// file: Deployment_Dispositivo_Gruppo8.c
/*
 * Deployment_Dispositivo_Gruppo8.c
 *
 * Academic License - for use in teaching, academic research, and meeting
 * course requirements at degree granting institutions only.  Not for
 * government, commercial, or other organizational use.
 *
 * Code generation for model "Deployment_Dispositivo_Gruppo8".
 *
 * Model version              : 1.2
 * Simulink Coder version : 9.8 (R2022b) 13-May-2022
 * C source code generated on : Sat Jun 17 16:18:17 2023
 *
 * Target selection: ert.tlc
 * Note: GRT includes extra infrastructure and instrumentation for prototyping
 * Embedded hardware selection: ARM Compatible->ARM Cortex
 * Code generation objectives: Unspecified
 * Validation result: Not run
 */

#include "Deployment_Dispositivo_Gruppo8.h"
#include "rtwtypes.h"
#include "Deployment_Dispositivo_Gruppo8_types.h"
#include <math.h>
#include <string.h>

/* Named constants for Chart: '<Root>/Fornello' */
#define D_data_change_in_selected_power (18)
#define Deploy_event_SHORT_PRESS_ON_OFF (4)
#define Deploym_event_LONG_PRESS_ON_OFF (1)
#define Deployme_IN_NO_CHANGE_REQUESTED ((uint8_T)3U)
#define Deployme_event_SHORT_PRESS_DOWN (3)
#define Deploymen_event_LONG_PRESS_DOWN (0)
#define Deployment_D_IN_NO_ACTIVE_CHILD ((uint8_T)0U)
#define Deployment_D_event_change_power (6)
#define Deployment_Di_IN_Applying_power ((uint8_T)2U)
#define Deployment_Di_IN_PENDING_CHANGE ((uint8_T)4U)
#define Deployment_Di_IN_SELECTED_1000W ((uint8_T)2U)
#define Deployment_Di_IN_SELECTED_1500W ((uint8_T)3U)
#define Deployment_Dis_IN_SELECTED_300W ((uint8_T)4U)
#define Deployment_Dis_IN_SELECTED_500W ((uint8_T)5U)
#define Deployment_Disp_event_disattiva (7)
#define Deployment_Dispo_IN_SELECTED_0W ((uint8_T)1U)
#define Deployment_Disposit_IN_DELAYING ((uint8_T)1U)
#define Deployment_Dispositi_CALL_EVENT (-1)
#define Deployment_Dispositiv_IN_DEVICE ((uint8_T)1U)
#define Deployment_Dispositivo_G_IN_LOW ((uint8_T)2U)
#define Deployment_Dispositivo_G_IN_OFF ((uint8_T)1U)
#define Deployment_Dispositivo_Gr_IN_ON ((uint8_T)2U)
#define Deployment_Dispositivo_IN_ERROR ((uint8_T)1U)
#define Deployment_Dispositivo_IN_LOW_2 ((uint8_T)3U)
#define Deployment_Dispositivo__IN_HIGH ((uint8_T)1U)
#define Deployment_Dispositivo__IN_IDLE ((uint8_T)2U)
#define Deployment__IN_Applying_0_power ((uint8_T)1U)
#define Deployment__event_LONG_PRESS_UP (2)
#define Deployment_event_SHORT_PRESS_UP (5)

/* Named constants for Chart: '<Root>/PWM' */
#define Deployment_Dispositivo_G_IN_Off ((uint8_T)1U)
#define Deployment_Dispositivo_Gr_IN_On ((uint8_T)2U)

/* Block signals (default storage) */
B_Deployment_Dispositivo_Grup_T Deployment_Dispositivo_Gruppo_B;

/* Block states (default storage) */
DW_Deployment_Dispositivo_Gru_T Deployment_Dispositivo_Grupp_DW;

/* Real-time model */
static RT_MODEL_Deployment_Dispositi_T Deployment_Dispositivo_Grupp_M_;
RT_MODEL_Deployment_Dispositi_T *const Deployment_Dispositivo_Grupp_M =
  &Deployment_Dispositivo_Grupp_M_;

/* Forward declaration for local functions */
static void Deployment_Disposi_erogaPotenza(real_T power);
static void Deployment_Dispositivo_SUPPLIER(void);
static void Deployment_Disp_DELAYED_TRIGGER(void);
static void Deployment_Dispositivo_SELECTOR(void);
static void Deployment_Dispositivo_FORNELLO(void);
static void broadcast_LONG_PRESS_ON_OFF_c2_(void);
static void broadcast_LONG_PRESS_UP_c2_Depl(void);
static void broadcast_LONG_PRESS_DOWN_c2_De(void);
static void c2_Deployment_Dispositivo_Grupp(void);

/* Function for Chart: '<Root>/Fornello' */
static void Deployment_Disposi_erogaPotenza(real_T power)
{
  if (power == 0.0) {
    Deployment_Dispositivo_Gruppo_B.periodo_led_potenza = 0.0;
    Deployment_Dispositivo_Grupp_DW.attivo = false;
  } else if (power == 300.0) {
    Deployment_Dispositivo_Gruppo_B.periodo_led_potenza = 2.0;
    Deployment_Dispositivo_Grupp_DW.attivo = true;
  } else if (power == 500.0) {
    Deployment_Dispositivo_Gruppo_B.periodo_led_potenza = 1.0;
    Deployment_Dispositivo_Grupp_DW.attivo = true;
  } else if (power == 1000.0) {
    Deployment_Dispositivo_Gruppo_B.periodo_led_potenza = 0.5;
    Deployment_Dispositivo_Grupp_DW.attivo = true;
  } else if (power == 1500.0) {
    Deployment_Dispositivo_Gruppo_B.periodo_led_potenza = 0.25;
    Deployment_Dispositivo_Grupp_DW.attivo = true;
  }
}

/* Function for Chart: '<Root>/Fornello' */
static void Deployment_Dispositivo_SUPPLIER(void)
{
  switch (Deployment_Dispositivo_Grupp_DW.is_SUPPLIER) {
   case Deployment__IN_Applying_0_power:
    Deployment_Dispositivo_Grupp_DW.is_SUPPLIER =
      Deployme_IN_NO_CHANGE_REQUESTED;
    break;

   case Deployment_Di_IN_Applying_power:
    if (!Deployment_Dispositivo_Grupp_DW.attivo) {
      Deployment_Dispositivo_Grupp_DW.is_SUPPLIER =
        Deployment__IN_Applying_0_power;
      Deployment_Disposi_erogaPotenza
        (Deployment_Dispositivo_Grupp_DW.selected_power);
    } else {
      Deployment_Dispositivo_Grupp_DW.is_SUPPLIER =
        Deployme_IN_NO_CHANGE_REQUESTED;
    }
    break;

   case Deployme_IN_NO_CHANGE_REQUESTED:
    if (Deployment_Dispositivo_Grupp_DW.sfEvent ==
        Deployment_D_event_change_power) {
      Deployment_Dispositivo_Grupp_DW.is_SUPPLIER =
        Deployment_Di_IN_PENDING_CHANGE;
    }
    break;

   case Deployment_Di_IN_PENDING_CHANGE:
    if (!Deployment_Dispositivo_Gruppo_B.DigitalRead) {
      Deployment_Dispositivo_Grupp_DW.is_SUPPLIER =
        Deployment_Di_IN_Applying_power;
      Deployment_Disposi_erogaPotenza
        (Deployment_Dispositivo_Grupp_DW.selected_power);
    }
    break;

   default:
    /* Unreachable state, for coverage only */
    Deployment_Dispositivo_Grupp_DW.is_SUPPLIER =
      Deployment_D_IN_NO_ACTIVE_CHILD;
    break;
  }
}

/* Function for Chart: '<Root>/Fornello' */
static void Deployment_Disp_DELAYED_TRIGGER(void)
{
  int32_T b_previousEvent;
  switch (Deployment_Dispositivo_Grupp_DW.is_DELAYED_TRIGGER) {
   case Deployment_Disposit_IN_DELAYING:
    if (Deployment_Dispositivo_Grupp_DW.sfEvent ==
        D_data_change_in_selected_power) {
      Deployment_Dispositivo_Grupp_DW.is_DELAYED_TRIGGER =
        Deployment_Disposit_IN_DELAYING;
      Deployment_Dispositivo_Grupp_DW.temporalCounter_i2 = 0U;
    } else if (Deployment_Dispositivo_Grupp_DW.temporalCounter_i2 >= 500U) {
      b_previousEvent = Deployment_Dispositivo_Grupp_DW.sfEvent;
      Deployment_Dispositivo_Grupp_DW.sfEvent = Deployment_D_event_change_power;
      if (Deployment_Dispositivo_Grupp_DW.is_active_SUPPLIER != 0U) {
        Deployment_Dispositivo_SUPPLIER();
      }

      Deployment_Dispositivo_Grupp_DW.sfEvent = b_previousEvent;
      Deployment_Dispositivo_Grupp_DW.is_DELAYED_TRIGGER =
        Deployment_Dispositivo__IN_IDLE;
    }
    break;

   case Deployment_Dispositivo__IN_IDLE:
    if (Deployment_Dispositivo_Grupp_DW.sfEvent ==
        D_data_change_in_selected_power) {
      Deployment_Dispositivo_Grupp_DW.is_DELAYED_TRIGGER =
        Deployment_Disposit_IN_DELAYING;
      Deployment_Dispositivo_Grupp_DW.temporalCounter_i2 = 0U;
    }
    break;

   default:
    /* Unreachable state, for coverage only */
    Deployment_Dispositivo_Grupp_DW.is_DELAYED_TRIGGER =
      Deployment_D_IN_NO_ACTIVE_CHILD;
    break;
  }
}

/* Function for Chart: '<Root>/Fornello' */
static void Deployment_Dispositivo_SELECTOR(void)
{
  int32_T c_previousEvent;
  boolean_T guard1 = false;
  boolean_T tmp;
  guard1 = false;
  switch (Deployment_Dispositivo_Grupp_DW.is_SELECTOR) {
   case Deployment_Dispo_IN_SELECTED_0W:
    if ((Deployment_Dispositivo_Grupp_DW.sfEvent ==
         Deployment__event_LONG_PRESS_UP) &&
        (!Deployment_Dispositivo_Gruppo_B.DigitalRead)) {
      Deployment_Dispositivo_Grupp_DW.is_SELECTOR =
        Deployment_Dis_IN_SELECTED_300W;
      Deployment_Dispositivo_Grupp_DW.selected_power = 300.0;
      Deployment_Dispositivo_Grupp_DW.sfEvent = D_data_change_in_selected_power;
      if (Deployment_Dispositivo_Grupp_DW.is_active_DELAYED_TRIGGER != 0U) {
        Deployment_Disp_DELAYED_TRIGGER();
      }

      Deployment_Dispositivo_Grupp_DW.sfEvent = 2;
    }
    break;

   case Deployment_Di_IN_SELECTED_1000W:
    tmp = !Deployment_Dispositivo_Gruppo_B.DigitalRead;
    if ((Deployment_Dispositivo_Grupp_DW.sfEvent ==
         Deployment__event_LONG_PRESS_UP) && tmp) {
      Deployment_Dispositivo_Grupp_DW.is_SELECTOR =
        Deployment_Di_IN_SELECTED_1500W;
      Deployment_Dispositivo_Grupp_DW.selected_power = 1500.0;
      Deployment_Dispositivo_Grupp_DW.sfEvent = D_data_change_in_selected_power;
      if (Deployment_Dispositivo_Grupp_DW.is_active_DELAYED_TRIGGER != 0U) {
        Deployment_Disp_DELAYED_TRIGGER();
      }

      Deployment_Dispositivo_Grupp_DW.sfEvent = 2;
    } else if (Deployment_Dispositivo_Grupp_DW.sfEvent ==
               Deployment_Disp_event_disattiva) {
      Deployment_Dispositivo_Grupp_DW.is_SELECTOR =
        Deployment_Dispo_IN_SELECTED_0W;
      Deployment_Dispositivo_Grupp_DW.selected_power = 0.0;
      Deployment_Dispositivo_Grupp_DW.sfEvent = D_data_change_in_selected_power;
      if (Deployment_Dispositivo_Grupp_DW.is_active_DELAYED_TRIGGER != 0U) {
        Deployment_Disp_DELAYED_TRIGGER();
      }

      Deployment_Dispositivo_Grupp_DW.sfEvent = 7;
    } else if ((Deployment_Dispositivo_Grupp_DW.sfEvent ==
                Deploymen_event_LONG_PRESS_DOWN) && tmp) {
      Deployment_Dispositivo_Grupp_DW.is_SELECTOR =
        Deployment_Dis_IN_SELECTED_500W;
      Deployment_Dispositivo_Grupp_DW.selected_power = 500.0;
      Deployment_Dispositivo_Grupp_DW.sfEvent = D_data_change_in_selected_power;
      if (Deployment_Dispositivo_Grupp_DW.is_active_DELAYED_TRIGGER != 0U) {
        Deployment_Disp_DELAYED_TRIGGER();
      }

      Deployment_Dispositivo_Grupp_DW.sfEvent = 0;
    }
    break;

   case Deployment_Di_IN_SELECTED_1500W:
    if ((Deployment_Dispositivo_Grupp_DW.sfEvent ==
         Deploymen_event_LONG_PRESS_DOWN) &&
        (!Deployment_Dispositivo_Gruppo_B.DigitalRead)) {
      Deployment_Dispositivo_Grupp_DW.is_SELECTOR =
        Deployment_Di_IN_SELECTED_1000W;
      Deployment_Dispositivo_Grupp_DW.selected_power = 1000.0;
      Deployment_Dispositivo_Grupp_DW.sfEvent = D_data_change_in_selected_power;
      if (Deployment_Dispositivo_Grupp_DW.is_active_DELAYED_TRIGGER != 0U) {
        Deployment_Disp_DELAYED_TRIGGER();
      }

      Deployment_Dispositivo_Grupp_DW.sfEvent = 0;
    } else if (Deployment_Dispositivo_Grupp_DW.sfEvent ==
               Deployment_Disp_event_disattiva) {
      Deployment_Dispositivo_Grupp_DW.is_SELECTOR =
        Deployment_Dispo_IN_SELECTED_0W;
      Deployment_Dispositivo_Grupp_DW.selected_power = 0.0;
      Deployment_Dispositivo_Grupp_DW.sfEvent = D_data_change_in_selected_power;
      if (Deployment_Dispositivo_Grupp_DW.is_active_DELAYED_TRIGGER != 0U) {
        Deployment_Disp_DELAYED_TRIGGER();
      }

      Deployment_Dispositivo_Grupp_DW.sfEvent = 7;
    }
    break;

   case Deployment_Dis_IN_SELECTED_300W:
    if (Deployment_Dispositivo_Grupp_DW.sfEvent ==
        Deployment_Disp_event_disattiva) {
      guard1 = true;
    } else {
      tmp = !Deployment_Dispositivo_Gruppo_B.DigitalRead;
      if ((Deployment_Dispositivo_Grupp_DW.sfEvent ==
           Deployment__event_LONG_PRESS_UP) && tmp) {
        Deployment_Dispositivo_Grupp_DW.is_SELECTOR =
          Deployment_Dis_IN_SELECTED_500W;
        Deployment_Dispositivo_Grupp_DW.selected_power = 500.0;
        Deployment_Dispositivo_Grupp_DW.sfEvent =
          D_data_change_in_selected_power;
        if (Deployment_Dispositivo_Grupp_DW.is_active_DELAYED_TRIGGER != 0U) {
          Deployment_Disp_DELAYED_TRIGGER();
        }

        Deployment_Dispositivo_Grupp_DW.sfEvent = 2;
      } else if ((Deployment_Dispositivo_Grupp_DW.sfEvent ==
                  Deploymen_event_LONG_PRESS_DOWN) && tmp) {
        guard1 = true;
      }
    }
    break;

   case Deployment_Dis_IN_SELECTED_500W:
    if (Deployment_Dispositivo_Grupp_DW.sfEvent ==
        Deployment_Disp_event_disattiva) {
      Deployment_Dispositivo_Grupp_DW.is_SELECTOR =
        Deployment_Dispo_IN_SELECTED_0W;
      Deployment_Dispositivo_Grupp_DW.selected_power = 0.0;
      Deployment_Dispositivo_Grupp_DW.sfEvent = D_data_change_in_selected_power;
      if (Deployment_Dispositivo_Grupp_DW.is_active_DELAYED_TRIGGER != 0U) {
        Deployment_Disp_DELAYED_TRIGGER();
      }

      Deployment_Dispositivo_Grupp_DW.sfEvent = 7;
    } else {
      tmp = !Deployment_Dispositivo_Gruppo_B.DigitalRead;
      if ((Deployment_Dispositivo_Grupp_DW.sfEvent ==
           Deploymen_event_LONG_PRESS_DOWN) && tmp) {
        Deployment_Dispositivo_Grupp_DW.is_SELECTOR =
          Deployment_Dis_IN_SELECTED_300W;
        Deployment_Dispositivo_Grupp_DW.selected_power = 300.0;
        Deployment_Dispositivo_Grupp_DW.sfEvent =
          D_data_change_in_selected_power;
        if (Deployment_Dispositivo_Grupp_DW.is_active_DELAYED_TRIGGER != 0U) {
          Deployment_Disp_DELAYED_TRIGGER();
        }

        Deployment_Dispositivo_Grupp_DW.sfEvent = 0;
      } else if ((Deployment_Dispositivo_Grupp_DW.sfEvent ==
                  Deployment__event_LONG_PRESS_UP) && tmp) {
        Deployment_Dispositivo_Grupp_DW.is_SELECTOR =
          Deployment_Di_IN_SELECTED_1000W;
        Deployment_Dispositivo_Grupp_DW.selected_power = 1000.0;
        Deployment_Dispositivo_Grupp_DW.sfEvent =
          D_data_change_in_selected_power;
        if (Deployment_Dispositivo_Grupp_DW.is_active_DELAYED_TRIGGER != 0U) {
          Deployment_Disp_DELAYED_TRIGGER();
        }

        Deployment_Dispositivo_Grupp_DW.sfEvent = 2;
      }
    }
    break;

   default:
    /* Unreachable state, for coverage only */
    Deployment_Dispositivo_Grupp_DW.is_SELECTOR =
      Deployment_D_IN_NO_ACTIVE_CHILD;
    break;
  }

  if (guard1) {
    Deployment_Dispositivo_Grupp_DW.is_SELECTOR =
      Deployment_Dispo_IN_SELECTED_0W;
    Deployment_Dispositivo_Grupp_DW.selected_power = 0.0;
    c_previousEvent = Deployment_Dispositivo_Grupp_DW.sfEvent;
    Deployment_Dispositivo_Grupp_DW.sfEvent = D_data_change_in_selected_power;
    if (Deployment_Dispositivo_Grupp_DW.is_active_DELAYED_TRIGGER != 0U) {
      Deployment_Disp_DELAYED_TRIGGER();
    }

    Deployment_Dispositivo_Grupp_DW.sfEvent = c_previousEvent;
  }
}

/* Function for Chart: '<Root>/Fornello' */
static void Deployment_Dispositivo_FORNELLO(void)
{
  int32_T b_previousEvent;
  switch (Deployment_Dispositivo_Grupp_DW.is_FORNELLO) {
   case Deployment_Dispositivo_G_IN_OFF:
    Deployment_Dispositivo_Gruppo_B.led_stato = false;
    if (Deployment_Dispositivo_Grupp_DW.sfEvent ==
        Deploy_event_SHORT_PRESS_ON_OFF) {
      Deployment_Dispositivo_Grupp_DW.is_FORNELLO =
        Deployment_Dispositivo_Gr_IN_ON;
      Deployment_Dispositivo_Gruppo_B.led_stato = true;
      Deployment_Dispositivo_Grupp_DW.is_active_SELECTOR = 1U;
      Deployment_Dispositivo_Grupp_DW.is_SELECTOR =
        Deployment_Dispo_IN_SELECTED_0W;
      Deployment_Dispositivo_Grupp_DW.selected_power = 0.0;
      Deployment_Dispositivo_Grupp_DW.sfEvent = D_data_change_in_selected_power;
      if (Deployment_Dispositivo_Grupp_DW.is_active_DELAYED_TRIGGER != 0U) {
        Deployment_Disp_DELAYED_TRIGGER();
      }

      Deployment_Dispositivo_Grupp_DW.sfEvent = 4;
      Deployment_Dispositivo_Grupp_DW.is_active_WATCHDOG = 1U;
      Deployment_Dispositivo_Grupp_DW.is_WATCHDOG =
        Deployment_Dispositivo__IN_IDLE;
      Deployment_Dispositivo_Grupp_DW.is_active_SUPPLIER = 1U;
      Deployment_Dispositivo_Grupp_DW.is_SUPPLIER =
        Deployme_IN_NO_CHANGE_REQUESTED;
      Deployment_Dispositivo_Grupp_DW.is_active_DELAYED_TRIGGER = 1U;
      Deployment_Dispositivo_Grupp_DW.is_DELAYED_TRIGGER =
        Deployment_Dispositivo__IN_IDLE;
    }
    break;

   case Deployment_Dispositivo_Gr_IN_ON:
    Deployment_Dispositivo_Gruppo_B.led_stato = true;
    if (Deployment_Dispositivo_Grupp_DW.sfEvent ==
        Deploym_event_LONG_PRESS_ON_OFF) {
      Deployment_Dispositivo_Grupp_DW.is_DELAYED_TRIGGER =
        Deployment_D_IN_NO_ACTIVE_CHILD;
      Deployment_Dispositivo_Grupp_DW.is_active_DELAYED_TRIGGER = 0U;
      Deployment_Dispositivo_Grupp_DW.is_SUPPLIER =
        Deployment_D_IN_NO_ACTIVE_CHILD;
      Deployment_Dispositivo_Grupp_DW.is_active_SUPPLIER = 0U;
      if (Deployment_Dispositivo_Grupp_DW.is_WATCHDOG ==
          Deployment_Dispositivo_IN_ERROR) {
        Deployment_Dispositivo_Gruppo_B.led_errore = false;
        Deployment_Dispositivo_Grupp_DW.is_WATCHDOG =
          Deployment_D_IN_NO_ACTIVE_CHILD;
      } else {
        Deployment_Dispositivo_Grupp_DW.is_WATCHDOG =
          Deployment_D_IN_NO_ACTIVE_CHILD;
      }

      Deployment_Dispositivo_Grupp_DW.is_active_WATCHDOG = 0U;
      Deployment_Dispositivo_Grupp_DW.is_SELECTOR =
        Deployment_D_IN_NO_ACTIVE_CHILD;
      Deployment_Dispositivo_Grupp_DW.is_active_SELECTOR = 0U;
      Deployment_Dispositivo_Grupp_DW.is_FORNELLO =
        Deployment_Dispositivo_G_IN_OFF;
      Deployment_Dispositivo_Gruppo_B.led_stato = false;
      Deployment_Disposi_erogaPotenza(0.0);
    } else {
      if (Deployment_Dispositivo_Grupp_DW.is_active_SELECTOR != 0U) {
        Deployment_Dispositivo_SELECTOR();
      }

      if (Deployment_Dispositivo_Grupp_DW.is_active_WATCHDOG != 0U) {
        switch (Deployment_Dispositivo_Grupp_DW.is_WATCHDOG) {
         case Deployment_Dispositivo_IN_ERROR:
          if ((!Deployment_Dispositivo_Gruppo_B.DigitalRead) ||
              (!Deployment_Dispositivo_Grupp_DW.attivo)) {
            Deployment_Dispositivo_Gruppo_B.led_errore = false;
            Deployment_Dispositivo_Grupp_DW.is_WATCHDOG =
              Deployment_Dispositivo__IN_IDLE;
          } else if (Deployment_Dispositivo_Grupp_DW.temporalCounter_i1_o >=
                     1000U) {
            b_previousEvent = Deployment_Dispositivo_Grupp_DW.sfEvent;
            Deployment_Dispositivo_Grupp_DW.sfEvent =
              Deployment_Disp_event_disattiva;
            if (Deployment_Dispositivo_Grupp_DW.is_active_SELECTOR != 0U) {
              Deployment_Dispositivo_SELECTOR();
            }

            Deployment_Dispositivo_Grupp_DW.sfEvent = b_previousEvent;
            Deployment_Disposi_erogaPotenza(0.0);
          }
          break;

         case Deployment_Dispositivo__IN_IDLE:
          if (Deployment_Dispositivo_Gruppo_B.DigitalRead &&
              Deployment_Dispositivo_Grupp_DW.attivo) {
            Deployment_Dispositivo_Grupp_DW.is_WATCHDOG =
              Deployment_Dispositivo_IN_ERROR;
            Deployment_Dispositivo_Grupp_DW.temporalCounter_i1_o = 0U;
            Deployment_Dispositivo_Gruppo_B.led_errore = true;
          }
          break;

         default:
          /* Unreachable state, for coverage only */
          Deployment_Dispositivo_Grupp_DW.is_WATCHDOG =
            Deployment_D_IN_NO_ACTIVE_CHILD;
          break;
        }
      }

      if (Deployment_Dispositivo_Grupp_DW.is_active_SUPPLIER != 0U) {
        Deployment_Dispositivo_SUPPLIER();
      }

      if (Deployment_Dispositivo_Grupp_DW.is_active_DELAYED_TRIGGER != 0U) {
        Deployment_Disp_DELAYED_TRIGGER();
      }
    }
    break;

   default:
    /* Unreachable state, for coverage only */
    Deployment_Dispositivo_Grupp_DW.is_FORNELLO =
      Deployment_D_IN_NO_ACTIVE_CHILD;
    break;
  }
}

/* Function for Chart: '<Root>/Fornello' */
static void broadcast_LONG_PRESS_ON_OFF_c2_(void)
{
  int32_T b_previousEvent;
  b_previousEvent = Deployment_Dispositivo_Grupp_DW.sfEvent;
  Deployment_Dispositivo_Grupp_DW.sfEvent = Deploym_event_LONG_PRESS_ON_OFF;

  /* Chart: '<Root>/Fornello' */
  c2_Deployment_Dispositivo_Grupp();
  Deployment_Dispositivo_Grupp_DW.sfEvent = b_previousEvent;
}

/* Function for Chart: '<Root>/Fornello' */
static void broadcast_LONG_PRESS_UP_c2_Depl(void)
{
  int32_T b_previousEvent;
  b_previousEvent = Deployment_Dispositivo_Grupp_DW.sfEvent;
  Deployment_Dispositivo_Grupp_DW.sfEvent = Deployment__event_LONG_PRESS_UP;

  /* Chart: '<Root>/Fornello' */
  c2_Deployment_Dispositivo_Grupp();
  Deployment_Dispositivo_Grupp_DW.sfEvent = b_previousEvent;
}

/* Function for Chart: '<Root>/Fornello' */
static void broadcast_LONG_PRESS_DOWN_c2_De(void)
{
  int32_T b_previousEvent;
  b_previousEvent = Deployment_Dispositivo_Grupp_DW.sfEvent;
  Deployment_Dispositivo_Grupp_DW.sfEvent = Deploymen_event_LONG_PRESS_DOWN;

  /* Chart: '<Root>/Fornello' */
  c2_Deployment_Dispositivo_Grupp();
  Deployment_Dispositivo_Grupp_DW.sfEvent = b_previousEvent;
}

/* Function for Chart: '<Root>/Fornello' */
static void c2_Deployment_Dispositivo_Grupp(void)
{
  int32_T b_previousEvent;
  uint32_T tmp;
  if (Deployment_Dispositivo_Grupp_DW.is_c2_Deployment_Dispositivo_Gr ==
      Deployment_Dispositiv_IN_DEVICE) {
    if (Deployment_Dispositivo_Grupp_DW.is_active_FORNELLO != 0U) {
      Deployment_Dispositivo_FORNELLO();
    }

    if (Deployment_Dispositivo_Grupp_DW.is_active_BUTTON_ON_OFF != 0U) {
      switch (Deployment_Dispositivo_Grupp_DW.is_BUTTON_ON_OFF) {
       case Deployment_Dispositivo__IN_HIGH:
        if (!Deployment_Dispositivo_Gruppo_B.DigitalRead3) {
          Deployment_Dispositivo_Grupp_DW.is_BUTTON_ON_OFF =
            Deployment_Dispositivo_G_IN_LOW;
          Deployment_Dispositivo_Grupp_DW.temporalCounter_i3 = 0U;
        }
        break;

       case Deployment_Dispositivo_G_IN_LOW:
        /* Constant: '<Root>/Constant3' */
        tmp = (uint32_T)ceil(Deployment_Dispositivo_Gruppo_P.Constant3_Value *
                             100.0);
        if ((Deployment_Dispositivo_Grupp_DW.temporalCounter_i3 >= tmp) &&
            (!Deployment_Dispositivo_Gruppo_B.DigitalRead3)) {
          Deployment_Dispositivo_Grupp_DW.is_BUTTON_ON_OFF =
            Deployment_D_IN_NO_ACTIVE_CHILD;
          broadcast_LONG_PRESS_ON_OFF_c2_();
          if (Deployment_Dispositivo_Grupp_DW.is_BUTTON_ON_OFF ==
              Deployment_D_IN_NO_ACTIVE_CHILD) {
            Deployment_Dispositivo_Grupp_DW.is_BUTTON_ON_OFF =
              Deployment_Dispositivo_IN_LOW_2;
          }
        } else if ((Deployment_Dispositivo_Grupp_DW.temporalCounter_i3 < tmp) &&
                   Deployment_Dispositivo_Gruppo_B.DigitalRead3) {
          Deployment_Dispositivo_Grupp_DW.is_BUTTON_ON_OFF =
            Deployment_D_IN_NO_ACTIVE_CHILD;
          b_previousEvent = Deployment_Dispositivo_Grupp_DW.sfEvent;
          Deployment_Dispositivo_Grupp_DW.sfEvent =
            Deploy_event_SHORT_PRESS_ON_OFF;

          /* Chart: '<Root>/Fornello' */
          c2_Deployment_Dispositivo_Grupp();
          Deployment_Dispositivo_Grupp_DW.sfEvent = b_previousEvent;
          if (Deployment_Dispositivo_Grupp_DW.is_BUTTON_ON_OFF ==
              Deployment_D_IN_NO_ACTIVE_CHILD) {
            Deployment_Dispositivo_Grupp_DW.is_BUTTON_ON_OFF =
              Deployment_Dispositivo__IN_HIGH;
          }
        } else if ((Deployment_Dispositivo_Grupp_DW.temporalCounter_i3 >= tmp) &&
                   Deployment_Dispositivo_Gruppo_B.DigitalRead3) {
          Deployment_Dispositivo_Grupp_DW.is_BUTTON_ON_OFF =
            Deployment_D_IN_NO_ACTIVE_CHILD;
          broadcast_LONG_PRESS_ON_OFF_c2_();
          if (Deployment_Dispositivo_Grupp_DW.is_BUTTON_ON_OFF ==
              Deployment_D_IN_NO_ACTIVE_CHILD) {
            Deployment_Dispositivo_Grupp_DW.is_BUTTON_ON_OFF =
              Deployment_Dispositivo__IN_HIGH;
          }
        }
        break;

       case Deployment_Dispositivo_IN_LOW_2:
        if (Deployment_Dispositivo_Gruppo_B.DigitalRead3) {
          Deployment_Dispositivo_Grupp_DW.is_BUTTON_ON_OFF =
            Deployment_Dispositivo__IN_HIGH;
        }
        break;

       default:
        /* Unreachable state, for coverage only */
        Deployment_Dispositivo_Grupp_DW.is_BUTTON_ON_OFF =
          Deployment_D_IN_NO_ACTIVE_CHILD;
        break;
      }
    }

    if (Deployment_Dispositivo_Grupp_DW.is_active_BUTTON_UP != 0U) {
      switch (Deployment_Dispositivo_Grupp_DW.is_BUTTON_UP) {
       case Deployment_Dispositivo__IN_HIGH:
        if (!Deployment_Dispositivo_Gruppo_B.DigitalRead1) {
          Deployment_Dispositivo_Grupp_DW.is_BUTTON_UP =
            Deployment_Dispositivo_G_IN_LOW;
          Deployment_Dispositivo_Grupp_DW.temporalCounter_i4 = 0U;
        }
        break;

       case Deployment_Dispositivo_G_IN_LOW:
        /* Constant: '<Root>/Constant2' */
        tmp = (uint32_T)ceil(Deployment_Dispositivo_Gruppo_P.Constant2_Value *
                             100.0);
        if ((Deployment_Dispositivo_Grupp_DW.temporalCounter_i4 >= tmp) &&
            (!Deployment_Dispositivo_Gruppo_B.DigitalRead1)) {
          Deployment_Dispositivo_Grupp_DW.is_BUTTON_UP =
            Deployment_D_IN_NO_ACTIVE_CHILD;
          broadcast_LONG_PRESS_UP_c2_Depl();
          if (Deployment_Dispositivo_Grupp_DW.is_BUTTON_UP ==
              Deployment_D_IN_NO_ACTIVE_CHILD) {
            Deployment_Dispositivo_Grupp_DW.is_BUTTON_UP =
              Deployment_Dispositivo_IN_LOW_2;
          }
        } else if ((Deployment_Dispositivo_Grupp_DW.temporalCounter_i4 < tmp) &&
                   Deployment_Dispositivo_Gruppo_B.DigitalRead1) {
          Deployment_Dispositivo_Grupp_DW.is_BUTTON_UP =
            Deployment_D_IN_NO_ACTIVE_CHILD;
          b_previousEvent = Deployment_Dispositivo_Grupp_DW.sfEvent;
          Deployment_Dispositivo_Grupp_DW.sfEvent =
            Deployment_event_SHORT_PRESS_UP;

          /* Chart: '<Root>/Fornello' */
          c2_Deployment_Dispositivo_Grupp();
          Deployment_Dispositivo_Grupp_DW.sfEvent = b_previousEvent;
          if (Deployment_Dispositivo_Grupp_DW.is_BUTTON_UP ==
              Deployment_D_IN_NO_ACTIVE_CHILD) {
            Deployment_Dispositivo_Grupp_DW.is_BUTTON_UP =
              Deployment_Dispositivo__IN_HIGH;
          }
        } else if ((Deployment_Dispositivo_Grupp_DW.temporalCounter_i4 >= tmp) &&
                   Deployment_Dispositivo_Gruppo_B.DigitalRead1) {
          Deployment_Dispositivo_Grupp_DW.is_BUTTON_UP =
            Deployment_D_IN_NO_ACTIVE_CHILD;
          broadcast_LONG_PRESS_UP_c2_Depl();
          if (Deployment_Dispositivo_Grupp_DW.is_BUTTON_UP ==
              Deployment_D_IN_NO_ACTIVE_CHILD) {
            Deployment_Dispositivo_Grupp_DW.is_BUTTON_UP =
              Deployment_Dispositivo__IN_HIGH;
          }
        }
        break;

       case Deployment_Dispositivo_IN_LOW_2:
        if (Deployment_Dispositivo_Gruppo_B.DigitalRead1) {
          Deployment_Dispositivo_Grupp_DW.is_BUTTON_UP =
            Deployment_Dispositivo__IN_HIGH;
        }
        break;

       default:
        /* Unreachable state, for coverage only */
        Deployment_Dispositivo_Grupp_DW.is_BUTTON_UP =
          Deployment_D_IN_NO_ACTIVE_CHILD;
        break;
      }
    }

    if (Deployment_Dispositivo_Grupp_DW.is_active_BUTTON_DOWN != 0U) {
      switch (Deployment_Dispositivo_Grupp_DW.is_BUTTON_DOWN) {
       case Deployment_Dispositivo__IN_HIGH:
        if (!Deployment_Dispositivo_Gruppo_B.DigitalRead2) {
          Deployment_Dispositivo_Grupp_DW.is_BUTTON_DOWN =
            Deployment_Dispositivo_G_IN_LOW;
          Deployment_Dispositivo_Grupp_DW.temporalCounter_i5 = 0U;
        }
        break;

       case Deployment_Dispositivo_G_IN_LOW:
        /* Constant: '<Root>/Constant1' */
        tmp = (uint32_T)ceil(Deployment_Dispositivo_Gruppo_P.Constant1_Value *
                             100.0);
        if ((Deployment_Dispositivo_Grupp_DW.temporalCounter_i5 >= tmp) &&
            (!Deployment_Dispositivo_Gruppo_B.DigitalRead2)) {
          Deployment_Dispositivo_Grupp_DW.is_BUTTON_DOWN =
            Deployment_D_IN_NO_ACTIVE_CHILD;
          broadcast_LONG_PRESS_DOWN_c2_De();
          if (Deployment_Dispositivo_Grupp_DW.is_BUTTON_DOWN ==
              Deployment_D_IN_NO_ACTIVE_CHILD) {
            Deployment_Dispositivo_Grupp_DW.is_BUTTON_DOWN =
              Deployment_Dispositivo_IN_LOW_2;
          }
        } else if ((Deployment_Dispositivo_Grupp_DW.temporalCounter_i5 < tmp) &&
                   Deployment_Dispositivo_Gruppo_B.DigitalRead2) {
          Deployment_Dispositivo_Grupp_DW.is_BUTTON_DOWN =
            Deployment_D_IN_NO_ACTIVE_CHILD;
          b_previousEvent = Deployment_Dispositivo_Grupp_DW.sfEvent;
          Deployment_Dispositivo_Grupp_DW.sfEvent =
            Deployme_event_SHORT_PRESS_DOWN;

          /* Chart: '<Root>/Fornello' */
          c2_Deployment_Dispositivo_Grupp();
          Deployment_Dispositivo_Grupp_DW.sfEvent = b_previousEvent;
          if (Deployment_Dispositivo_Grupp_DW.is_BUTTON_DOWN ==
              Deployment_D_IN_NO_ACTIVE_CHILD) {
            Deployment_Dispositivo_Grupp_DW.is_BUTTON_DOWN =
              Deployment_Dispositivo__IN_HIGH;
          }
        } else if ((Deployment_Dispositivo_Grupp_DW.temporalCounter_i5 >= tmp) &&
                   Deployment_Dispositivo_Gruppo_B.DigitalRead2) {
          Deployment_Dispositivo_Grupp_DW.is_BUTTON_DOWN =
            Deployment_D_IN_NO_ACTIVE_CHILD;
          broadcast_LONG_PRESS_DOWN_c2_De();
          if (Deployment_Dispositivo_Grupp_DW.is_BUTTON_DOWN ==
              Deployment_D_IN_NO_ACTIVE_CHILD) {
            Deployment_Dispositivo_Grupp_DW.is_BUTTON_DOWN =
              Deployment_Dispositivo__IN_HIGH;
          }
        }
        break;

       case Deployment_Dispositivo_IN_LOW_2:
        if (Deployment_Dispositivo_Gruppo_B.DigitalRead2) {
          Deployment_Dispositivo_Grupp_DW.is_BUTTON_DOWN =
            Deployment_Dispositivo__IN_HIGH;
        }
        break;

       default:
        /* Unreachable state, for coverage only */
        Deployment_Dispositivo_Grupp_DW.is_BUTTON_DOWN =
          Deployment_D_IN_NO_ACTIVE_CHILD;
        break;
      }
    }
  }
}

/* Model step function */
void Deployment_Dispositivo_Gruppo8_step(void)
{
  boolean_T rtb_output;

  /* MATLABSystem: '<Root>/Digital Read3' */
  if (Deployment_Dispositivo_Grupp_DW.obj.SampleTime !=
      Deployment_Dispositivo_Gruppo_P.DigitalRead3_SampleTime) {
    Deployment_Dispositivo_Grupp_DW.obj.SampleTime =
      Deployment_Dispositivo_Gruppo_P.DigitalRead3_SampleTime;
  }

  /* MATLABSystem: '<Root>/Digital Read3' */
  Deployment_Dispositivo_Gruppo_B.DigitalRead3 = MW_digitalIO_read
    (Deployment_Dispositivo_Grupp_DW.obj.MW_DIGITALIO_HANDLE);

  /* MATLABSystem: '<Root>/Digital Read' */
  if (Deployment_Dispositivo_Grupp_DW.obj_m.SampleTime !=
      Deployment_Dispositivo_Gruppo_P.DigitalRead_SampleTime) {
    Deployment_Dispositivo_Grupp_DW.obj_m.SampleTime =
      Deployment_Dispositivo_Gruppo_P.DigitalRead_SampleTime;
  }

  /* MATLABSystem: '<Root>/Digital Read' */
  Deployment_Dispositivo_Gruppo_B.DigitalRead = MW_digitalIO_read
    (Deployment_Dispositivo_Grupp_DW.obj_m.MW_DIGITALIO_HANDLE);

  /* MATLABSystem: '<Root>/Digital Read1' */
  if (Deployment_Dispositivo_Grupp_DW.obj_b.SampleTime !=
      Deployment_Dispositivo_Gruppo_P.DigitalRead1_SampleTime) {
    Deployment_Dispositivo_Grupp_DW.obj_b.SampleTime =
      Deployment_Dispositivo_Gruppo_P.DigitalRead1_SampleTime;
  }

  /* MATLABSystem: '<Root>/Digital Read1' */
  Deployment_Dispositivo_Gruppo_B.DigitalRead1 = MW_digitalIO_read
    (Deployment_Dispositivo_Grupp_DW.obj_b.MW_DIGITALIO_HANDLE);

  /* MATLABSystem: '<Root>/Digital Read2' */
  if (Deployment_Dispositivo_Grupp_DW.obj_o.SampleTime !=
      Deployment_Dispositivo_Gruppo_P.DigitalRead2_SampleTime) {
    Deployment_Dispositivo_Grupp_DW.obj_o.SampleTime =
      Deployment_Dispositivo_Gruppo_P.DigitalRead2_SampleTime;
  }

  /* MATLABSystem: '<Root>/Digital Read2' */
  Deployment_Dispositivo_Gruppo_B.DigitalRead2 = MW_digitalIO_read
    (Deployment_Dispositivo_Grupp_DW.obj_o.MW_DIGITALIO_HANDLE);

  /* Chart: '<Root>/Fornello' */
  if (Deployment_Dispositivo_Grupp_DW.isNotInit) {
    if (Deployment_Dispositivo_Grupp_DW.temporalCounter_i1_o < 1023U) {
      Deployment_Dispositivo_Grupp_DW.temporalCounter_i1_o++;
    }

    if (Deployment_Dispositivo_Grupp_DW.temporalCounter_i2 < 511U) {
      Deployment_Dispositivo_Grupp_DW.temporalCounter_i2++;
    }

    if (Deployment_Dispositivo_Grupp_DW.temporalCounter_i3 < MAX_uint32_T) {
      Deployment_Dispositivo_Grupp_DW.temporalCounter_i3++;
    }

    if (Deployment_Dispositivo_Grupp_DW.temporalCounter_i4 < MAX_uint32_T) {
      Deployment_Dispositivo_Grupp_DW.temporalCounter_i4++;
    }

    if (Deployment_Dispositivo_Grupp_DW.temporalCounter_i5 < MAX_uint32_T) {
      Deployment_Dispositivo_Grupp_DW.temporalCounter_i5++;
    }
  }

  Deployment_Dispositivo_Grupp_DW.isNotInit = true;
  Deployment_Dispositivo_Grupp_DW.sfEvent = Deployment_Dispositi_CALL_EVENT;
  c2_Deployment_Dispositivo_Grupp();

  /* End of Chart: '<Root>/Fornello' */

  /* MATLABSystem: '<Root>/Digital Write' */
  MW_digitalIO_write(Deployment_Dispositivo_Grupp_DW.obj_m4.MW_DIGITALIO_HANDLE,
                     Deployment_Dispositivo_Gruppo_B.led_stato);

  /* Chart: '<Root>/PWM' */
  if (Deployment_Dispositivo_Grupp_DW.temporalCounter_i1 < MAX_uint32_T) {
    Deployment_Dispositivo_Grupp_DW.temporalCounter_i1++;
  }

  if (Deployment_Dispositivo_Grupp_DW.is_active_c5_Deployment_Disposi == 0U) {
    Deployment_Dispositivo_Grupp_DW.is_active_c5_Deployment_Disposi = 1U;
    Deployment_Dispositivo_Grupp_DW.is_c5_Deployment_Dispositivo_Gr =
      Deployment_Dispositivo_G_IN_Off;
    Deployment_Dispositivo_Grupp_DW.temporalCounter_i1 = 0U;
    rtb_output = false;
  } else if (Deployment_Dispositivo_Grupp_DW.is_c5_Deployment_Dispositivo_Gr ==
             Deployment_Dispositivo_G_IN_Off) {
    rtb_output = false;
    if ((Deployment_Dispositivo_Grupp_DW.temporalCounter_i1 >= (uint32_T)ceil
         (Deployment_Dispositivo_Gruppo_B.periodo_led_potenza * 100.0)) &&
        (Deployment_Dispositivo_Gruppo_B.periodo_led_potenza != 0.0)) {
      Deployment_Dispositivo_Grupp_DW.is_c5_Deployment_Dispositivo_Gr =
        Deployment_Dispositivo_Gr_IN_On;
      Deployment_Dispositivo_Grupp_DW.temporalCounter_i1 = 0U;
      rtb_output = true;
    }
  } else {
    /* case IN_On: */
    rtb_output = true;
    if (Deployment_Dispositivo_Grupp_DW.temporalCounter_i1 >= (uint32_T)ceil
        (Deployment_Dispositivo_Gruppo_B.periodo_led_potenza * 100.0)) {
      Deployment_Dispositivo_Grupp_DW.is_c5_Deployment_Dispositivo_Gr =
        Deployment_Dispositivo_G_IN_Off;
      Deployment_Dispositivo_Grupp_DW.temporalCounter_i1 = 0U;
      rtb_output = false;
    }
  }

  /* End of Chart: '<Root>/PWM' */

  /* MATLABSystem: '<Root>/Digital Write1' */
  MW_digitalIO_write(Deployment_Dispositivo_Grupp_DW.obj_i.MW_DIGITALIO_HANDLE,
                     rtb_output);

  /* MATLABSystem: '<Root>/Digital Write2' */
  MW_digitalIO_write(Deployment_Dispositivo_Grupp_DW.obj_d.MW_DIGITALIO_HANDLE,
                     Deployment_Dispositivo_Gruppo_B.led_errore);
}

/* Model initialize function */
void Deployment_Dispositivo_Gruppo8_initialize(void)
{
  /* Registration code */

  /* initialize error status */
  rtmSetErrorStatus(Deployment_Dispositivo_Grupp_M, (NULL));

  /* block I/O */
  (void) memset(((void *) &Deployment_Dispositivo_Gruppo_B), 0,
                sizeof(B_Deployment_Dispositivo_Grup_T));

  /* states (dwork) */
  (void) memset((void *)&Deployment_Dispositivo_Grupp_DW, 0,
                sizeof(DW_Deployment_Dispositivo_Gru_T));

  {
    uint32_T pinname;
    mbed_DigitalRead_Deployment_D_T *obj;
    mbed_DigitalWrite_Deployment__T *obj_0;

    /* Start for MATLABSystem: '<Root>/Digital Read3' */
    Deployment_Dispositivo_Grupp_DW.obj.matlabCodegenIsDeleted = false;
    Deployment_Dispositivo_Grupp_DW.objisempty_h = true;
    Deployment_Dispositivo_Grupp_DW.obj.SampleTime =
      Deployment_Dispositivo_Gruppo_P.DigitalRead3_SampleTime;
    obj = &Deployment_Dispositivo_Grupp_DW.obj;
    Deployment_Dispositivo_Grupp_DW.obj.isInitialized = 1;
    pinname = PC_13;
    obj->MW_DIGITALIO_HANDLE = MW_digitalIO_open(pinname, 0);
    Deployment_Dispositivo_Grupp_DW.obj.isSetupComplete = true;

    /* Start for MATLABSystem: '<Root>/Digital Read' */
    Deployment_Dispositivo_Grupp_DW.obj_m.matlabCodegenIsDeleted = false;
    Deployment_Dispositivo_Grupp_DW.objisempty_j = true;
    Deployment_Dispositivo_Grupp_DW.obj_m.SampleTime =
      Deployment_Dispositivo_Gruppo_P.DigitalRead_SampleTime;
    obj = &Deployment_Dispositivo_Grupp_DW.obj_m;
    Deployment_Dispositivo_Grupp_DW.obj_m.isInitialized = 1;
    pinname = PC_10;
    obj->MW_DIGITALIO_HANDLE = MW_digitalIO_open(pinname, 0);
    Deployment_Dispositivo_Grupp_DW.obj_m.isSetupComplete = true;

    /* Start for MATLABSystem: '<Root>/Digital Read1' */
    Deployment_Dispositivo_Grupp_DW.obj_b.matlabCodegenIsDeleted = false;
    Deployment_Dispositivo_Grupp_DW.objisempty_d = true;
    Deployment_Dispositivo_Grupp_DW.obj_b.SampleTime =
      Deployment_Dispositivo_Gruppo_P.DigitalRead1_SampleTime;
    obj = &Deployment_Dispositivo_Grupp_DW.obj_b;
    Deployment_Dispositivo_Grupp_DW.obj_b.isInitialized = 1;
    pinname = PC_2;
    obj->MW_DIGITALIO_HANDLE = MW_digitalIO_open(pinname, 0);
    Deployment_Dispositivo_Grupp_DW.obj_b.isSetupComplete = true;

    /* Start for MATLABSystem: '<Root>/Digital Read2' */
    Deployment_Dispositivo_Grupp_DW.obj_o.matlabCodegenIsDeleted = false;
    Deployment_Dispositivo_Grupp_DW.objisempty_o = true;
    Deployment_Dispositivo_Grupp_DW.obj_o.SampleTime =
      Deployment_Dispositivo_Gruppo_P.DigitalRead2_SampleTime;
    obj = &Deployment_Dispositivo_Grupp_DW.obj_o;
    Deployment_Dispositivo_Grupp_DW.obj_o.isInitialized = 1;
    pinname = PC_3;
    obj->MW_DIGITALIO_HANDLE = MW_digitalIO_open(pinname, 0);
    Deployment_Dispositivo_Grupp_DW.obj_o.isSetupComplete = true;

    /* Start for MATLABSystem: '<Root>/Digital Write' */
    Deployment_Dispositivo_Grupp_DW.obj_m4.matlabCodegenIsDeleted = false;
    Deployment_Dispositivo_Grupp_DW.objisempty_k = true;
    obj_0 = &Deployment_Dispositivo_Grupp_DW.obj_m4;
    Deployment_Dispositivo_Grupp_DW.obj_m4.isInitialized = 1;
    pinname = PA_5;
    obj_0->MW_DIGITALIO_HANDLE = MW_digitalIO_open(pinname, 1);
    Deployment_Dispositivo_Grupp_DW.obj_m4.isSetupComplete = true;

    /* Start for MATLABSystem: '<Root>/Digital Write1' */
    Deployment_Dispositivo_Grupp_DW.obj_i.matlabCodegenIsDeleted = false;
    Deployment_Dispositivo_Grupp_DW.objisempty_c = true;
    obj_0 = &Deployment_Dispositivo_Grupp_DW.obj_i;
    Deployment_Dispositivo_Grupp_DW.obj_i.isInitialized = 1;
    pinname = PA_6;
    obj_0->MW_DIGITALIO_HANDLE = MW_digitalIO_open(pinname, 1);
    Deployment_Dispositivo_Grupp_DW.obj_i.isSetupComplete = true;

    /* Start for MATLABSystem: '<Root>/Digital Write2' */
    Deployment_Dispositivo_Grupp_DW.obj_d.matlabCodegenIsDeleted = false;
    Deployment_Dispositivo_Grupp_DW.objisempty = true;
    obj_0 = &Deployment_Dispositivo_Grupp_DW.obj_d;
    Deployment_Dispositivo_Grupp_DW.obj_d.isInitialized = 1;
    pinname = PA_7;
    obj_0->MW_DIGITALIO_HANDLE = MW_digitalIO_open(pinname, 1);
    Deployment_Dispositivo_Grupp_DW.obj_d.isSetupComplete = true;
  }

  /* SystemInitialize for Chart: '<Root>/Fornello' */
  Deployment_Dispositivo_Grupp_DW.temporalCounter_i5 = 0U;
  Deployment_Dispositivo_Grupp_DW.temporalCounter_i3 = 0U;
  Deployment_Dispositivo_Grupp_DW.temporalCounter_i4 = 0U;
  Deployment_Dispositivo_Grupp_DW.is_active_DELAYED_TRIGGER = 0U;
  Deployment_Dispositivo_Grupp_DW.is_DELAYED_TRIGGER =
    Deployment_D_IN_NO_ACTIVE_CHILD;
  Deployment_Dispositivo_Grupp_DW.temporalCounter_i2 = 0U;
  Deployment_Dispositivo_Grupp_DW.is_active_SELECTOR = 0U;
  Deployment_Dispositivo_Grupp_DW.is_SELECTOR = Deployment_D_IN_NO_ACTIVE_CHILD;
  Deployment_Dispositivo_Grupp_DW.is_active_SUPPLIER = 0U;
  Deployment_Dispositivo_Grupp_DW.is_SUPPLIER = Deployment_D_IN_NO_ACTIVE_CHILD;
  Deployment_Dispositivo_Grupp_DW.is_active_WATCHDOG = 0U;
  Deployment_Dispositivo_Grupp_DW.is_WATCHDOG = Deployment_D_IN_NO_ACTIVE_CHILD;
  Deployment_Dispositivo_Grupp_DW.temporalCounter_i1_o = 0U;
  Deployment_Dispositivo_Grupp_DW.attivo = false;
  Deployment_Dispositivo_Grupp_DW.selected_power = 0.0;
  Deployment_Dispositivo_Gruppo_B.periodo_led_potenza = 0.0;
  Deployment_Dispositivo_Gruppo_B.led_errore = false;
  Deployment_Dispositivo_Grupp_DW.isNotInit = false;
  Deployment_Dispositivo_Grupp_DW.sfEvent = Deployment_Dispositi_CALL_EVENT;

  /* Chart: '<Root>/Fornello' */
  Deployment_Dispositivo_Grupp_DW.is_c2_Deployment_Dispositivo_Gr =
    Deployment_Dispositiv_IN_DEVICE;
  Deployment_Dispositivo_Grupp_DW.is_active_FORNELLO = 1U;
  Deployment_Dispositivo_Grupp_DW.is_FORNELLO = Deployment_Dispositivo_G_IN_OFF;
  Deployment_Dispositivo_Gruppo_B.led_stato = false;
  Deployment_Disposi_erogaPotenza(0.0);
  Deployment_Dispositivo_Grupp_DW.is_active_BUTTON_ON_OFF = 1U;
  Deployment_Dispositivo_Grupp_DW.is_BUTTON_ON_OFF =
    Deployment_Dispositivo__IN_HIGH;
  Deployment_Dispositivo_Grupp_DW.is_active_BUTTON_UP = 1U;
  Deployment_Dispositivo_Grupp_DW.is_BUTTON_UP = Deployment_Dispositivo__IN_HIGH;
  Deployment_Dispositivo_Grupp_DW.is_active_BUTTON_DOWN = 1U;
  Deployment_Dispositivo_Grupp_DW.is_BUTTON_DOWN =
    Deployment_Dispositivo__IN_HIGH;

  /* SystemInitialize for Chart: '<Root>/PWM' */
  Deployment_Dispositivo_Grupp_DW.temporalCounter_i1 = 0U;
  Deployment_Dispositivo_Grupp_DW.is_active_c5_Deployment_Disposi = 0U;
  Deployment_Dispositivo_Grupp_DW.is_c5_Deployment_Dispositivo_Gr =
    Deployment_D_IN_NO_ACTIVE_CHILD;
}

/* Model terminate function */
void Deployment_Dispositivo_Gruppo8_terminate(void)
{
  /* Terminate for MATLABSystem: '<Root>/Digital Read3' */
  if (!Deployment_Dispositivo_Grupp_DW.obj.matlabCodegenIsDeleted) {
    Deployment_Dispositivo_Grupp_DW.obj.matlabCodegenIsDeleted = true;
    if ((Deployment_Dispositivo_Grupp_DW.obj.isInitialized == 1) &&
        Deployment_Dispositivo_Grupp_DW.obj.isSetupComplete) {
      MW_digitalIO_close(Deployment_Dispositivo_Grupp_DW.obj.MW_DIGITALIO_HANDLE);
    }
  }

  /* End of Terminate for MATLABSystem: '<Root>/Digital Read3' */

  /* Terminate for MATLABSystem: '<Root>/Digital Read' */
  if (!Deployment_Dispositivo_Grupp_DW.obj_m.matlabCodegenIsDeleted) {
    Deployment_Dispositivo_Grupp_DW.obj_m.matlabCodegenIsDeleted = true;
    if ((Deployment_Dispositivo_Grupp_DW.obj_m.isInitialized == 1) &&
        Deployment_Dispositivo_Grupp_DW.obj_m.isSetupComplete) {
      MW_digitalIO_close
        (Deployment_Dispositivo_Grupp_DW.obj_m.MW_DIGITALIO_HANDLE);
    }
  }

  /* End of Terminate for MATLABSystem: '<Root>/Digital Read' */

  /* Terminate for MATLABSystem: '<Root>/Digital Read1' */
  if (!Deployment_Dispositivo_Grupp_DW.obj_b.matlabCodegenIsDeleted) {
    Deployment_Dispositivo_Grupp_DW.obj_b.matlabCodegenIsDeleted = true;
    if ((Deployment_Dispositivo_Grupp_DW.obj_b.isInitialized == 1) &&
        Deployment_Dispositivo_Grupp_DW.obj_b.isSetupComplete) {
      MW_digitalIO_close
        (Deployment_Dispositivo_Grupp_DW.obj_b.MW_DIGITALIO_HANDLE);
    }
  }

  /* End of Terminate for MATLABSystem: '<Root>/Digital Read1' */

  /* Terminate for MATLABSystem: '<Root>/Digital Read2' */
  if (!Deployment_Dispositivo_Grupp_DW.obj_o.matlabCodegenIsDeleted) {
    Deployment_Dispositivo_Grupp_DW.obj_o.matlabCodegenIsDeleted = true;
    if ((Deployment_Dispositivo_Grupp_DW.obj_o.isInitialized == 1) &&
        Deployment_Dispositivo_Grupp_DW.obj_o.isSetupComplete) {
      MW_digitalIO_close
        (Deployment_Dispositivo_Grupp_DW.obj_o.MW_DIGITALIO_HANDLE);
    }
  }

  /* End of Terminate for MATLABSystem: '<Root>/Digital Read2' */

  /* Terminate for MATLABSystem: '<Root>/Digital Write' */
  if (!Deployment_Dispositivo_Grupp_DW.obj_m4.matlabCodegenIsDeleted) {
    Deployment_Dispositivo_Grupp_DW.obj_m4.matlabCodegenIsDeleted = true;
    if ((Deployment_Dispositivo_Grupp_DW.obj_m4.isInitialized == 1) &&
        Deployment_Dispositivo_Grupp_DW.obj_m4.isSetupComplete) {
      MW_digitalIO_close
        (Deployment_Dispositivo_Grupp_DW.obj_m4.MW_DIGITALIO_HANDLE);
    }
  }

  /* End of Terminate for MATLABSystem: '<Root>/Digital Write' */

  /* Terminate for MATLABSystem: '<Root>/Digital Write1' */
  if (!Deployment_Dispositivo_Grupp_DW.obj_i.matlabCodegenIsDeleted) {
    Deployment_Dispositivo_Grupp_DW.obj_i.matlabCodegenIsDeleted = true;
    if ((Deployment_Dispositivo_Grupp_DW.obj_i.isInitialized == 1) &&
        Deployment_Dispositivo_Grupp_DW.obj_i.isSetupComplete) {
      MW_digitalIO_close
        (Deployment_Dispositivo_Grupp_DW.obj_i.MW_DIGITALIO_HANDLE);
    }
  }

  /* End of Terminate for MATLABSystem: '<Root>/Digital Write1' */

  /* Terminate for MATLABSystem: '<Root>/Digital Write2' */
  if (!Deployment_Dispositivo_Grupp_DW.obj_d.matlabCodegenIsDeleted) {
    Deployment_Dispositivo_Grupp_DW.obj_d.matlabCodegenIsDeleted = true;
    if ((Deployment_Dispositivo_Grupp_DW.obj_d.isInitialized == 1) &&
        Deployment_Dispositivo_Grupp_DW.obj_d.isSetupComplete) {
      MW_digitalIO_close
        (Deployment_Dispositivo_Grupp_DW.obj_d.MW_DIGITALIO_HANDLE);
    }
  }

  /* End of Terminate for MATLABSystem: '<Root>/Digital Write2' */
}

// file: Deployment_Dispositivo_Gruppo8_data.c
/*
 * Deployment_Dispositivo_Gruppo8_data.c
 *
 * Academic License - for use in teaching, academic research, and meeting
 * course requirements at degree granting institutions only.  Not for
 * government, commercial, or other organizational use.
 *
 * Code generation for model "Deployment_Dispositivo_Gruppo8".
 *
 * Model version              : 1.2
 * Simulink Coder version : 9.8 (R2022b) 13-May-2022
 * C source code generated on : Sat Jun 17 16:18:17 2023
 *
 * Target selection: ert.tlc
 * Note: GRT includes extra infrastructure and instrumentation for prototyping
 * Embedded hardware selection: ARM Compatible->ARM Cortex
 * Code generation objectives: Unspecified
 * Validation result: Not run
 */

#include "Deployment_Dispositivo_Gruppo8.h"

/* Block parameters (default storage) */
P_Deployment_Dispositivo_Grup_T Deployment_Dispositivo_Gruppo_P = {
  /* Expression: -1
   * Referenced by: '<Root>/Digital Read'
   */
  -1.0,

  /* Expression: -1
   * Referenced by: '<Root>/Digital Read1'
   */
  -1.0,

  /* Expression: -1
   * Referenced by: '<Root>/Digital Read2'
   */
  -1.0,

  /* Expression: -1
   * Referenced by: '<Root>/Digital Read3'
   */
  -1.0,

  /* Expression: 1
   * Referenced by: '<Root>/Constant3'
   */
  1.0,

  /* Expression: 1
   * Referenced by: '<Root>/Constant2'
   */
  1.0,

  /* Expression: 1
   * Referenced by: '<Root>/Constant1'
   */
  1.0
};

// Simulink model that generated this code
simulink model "Deployment_Dispositivo_Gruppo8"  (R2022b)
settings: Solver=FixedStepAuto  StartTime=0.0  StopTime=inf  FixedStep=0.01  RelTol=1e-3  EnableMultiTasking=on
libraries: mbedblockslib x7

== system Deployment_Dispositivo_Gruppo8 ==
  Constant1 : Constant
  Constant2 : Constant
  Constant3 : Constant
  Digital Read : mbedblockslib/Digital Read  Pin=PC_10  Direction=input  SampleTime=-1
  Digital Read1 : mbedblockslib/Digital Read  Pin=PC_2  Direction=input  SampleTime=-1
  Digital Read2 : mbedblockslib/Digital Read  Pin=PC_3  Direction=input  SampleTime=-1
  Digital Read3 : mbedblockslib/Digital Read  Pin=PC_13  Direction=input  SampleTime=-1
  Digital Write : mbedblockslib/Digital Write  Pin=PA_5  Direction=output
  Digital Write1 : mbedblockslib/Digital Write  Pin=PA_6  Direction=output
  Digital Write2 : mbedblockslib/Digital Write  Pin=PA_7  Direction=output
  Fornello : Stateflow chart  TreatAsAtomicUnit=on
  PWM : Stateflow chart  TreatAsAtomicUnit=on
  wires:
  Fornello/1(led_stato) -> Digital Write/1
  Fornello/3(led_errore) -> Digital Write2/1
  Fornello/2(periodo_led_potenza) -> PWM/1(period)
  PWM/1(output) -> Digital Write1/1
  Constant1/1 -> Fornello/7(DEBOUNCE_DOWN)
  Constant2/1 -> Fornello/6(DEBOUNCE_UP)
  Constant3/1 -> Fornello/5(DEBOUNCE_ON_OFF)
  Digital Read1/1 -> Fornello/3(SIGNAL_UP)
  Digital Read/1 -> Fornello/2(pentola)
  Digital Read2/1 -> Fornello/4(SIGNAL_DOWN)
  Digital Read3/1 -> Fornello/1(SIGNAL_ON_OFF)

== stateflow chart Deployment_Dispositivo_Gruppo8/Fornello ==
  settings: executeAtInitialization=1
  state DEVICE
    state FORNELLO [parallel]
      settings: executionOrder=1
      state ON
        en: led_stato = true
        state SELECTOR [parallel]
          settings: executionOrder=1
          state SELECTED_0W
            en: selected_power=0;
          state SELECTED_300W
            en: selected_power=300;
          state SELECTED_500W
            en: selected_power=500
          state SELECTED_1000W
            en: selected_power=1000
          state SELECTED_1500W
            en: selected_power=1500
          (default) -> SELECTED_0W
          (junction 32) -> SELECTED_0W
          SELECTED_500W -> (junction 32) [order 1] : disattiva
          SELECTED_1000W -> (junction 32) [order 2] : disattiva
          SELECTED_1500W -> (junction 32) [order 2] : disattiva
          SELECTED_300W -> (junction 32) [order 1] : disattiva
          SELECTED_0W -> SELECTED_300W : LONG_PRESS_UP[pentola == false]
          SELECTED_300W -> SELECTED_0W [order 3] : LONG_PRESS_DOWN[pentola==false]
          SELECTED_500W -> SELECTED_300W [order 2] : LONG_PRESS_DOWN[pentola==false]
          SELECTED_300W -> SELECTED_500W [order 2] : LONG_PRESS_UP[pentola == false]
          SELECTED_1000W -> SELECTED_500W [order 3] : LONG_PRESS_DOWN[pentola==false]
          SELECTED_500W -> SELECTED_1000W [order 3] : LONG_PRESS_UP[pentola == false]
          SELECTED_1500W -> SELECTED_1000W [order 1] : LONG_PRESS_DOWN[pentola == false]
          SELECTED_1000W -> SELECTED_1500W [order 1] : LONG_PRESS_UP[pentola==false]
        state WATCHDOG [parallel]
          settings: executionOrder=2
          state IDLE
          state ERROR
            en: led_errore = true
            on after(10,sec): send(disattiva,SELECTOR); erogaPotenza(0)
            ex: led_errore = false
          (default) -> DEVICE.FORNELLO.ON.WATCHDOG.IDLE
          DEVICE.FORNELLO.ON.WATCHDOG.IDLE -> ERROR : [pentola == true && attivo==true]
          ERROR -> DEVICE.FORNELLO.ON.WATCHDOG.IDLE : [pentola == false || attivo == false]
        state SUPPLIER [parallel]
          settings: executionOrder=3
          state NO_CHANGE_REQUESTED
          state Applying_0_power
            en: erogaPotenza(selected_power)
          state Applying_power
            en: erogaPotenza(selected_power)
          state PENDING_CHANGE
            en: t_debug = 0
          NO_CHANGE_REQUESTED -> PENDING_CHANGE : change_power
          Applying_power -> NO_CHANGE_REQUESTED [order 2]
          Applying_0_power -> NO_CHANGE_REQUESTED
          Applying_power -> Applying_0_power [order 1] : [attivo == false]
          PENDING_CHANGE -> Applying_power : [pentola==false]
        state DELAYED_TRIGGER [parallel]
          settings: executionOrder=4
          state IDLE
          state DELAYING
          (default) -> DEVICE.FORNELLO.ON.DELAYED_TRIGGER.IDLE
          DEVICE.FORNELLO.ON.DELAYED_TRIGGER.IDLE -> DELAYING : change(selected_power)
          DELAYING -> DEVICE.FORNELLO.ON.DELAYED_TRIGGER.IDLE [order 2] : after(5,sec)/{send(change_power, SUPPLIER)}
          DELAYING -> DELAYING [order 1] : change(selected_power)
        (default) -> NO_CHANGE_REQUESTED
      state OFF
        en: led_stato = false; erogaPotenza(0)
      state erogaPotenza(power) [function]
        (default) -> (junction 65) : {power = double(power)}
        (junction 65) -> (junction 68) [order 1] : [power == 0]
        (junction 68) -> (junction 118) : {periodo_led_potenza=0;attivo=false}
        (junction 118) -> (junction 89)
        (junction 65) -> (junction 77) [order 2]
        (junction 77) -> (junction 83) [order 1] : [power == 300]
        (junction 83) -> (junction 120) : {periodo_led_potenza=2;attivo=true}
        (junction 120) -> (junction 89)
        (junction 77) -> (junction 79) [order 2]
        (junction 122) -> (junction 89)
        (junction 119) -> (junction 89)
        (junction 121) -> (junction 89)
        (junction 79) -> (junction 84) [order 1] : [power == 500]
        (junction 84) -> (junction 122) : {periodo_led_potenza=1;attivo=true}
        (junction 79) -> (junction 81) [order 2]
        (junction 81) -> (junction 92) [order 1] : [power == 1000]
        (junction 92) -> (junction 119) : {periodo_led_potenza=0.5;attivo=true}
        (junction 81) -> (junction 95) [order 2]
        (junction 95) -> (junction 99) : [power == 1500]
        (junction 99) -> (junction 121) : {periodo_led_potenza=0.25;attivo=true}
      (default) -> OFF
      OFF -> ON : SHORT_PRESS_ON_OFF
      ON -> OFF : LONG_PRESS_ON_OFF
    state BUTTON_ON_OFF [parallel]
      settings: executionOrder=2
      state HIGH
      state LOW_2
      state LOW
      (default) -> DEVICE.BUTTON_ON_OFF.HIGH
      DEVICE.BUTTON_ON_OFF.LOW_2 -> DEVICE.BUTTON_ON_OFF.HIGH : [SIGNAL_ON_OFF == true]
      DEVICE.BUTTON_ON_OFF.HIGH -> DEVICE.BUTTON_ON_OFF.LOW : [SIGNAL_ON_OFF == false]
      DEVICE.BUTTON_ON_OFF.LOW -> DEVICE.BUTTON_ON_OFF.HIGH [order 2] : before(DEBOUNCE_ON_OFF,sec)[SIGNAL_ON_OFF == true]/{send(SHORT_PRESS_ON_OFF)}
      DEVICE.BUTTON_ON_OFF.LOW -> DEVICE.BUTTON_ON_OFF.HIGH [order 3] : after(DEBOUNCE_ON_OFF,sec)[SIGNAL_ON_OFF == true]/{send(LONG_PRESS_ON_OFF)}
      DEVICE.BUTTON_ON_OFF.LOW -> DEVICE.BUTTON_ON_OFF.LOW_2 [order 1] : after(DEBOUNCE_ON_OFF,sec)[SIGNAL_ON_OFF == false]/{send(LONG_PRESS_ON_OFF)}
    state BUTTON_UP [parallel]
      settings: executionOrder=3
      state HIGH
      state LOW_2
      state LOW
      (default) -> DEVICE.BUTTON_UP.HIGH
      DEVICE.BUTTON_UP.LOW_2 -> DEVICE.BUTTON_UP.HIGH : [SIGNAL_UP == true]
      DEVICE.BUTTON_UP.HIGH -> DEVICE.BUTTON_UP.LOW : [SIGNAL_UP == false]
      DEVICE.BUTTON_UP.LOW -> DEVICE.BUTTON_UP.HIGH [order 2] : before(DEBOUNCE_UP,sec)[SIGNAL_UP == true]/{send(SHORT_PRESS_UP)}
      DEVICE.BUTTON_UP.LOW -> DEVICE.BUTTON_UP.HIGH [order 3] : after(DEBOUNCE_UP,sec)[SIGNAL_UP == true]/{send(LONG_PRESS_UP)}
      DEVICE.BUTTON_UP.LOW -> DEVICE.BUTTON_UP.LOW_2 [order 1] : after(DEBOUNCE_UP,sec)[SIGNAL_UP == false]/{send(LONG_PRESS_UP)}
    state BUTTON_DOWN [parallel]
      settings: executionOrder=4
      state HIGH
      state LOW_2
      state LOW
      (default) -> DEVICE.BUTTON_DOWN.HIGH
      DEVICE.BUTTON_DOWN.LOW_2 -> DEVICE.BUTTON_DOWN.HIGH : [SIGNAL_DOWN == true]
      DEVICE.BUTTON_DOWN.HIGH -> DEVICE.BUTTON_DOWN.LOW : [SIGNAL_DOWN == false]
      DEVICE.BUTTON_DOWN.LOW -> DEVICE.BUTTON_DOWN.HIGH [order 2] : before(DEBOUNCE_DOWN,sec)[SIGNAL_DOWN == true]/{send(SHORT_PRESS_DOWN)}
      DEVICE.BUTTON_DOWN.LOW -> DEVICE.BUTTON_DOWN.HIGH [order 3] : after(DEBOUNCE_DOWN,sec)[SIGNAL_DOWN == true]/{send(LONG_PRESS_DOWN)}
      DEVICE.BUTTON_DOWN.LOW -> DEVICE.BUTTON_DOWN.LOW_2 [order 1] : after(DEBOUNCE_DOWN,sec)[SIGNAL_DOWN == false]/{send(LONG_PRESS_DOWN)}
  (default) -> DEVICE
  data: power function_input double size=1; SIGNAL_ON_OFF input; attivo local boolean size=1 =false; led_stato output boolean size=1 =false; periodo_led_potenza output double size=1 =0; led_errore output boolean size=1 =false; pentola input boolean size=1; SIGNAL_UP input; SIGNAL_DOWN input; DEBOUNCE_ON_OFF input double; DEBOUNCE_UP input double; selected_power local double size=1 =0; t_debug local double =1; last_down local; last_up local; DEBOUNCE_DOWN input double; last_on_off local; debug local; flag local =0; last_value local
  events: disattiva local FUNCTION_CALL_EVENT; change_power local FUNCTION_CALL_EVENT; LONG_PRESS_DOWN local FUNCTION_CALL_EVENT; LONG_PRESS_UP local FUNCTION_CALL_EVENT; SHORT_PRESS_DOWN local FUNCTION_CALL_EVENT; SHORT_PRESS_UP local FUNCTION_CALL_EVENT; LONG_PRESS_ON_OFF local FUNCTION_CALL_EVENT; SHORT_PRESS_ON_OFF local FUNCTION_CALL_EVENT

== stateflow chart Deployment_Dispositivo_Gruppo8/PWM ==
  state Off
    en: output = false
  state On
    en: output = true
  (default) -> Off
  Off -> On : after(period,sec)[period ~= 0]
  On -> Off : after(period,sec)
  data: output output boolean size=1 =false; period input double size=1
